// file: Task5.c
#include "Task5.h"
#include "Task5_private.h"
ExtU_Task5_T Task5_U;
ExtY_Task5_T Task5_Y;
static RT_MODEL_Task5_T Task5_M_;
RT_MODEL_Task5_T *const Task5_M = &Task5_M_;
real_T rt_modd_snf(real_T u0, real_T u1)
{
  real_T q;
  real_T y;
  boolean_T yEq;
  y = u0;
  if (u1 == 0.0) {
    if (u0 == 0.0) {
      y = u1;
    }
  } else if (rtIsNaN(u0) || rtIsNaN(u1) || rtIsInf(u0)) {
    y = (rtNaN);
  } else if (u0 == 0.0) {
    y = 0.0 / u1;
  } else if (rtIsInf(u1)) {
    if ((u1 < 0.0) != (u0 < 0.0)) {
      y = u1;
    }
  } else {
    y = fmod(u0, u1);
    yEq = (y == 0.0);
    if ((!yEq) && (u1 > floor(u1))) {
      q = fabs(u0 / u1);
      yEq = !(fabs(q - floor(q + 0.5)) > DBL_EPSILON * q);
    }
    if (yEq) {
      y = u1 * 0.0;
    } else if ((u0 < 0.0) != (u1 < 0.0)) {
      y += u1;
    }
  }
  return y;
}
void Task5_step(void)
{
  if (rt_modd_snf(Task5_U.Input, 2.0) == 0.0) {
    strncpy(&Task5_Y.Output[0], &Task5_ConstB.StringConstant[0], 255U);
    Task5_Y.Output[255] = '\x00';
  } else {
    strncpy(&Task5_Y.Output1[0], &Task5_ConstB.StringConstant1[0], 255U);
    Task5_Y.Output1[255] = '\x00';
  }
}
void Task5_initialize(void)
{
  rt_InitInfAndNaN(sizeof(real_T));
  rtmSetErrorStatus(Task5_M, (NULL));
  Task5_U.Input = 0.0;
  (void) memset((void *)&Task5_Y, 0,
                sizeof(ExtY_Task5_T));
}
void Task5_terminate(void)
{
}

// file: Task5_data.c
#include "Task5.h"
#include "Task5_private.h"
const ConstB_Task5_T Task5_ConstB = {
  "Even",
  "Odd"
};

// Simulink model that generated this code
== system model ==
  Input : Inport
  Output : Outport  <- 1: Subsystem#1
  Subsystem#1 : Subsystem  <- 1: StringConstant, Action: If#1
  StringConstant : StringConstant
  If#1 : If  IfExpression=u1 == 0  <- 1: Math#1
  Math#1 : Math  Operator=mod  <- 1: Input, 2: Constant#1
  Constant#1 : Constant  Value=2
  Output1 : Outport  <- 1: Subsystem#2
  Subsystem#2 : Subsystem  <- 1: StringConstant1, Action: If#1/2
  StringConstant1 : StringConstant
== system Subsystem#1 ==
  Inport#1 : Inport
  ActionPort#1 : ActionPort
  Outport#1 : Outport  <- 1: Inport#1
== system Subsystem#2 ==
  Inport#2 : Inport
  ActionPort#2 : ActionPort
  Outport#2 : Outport  <- 1: Inport#2
